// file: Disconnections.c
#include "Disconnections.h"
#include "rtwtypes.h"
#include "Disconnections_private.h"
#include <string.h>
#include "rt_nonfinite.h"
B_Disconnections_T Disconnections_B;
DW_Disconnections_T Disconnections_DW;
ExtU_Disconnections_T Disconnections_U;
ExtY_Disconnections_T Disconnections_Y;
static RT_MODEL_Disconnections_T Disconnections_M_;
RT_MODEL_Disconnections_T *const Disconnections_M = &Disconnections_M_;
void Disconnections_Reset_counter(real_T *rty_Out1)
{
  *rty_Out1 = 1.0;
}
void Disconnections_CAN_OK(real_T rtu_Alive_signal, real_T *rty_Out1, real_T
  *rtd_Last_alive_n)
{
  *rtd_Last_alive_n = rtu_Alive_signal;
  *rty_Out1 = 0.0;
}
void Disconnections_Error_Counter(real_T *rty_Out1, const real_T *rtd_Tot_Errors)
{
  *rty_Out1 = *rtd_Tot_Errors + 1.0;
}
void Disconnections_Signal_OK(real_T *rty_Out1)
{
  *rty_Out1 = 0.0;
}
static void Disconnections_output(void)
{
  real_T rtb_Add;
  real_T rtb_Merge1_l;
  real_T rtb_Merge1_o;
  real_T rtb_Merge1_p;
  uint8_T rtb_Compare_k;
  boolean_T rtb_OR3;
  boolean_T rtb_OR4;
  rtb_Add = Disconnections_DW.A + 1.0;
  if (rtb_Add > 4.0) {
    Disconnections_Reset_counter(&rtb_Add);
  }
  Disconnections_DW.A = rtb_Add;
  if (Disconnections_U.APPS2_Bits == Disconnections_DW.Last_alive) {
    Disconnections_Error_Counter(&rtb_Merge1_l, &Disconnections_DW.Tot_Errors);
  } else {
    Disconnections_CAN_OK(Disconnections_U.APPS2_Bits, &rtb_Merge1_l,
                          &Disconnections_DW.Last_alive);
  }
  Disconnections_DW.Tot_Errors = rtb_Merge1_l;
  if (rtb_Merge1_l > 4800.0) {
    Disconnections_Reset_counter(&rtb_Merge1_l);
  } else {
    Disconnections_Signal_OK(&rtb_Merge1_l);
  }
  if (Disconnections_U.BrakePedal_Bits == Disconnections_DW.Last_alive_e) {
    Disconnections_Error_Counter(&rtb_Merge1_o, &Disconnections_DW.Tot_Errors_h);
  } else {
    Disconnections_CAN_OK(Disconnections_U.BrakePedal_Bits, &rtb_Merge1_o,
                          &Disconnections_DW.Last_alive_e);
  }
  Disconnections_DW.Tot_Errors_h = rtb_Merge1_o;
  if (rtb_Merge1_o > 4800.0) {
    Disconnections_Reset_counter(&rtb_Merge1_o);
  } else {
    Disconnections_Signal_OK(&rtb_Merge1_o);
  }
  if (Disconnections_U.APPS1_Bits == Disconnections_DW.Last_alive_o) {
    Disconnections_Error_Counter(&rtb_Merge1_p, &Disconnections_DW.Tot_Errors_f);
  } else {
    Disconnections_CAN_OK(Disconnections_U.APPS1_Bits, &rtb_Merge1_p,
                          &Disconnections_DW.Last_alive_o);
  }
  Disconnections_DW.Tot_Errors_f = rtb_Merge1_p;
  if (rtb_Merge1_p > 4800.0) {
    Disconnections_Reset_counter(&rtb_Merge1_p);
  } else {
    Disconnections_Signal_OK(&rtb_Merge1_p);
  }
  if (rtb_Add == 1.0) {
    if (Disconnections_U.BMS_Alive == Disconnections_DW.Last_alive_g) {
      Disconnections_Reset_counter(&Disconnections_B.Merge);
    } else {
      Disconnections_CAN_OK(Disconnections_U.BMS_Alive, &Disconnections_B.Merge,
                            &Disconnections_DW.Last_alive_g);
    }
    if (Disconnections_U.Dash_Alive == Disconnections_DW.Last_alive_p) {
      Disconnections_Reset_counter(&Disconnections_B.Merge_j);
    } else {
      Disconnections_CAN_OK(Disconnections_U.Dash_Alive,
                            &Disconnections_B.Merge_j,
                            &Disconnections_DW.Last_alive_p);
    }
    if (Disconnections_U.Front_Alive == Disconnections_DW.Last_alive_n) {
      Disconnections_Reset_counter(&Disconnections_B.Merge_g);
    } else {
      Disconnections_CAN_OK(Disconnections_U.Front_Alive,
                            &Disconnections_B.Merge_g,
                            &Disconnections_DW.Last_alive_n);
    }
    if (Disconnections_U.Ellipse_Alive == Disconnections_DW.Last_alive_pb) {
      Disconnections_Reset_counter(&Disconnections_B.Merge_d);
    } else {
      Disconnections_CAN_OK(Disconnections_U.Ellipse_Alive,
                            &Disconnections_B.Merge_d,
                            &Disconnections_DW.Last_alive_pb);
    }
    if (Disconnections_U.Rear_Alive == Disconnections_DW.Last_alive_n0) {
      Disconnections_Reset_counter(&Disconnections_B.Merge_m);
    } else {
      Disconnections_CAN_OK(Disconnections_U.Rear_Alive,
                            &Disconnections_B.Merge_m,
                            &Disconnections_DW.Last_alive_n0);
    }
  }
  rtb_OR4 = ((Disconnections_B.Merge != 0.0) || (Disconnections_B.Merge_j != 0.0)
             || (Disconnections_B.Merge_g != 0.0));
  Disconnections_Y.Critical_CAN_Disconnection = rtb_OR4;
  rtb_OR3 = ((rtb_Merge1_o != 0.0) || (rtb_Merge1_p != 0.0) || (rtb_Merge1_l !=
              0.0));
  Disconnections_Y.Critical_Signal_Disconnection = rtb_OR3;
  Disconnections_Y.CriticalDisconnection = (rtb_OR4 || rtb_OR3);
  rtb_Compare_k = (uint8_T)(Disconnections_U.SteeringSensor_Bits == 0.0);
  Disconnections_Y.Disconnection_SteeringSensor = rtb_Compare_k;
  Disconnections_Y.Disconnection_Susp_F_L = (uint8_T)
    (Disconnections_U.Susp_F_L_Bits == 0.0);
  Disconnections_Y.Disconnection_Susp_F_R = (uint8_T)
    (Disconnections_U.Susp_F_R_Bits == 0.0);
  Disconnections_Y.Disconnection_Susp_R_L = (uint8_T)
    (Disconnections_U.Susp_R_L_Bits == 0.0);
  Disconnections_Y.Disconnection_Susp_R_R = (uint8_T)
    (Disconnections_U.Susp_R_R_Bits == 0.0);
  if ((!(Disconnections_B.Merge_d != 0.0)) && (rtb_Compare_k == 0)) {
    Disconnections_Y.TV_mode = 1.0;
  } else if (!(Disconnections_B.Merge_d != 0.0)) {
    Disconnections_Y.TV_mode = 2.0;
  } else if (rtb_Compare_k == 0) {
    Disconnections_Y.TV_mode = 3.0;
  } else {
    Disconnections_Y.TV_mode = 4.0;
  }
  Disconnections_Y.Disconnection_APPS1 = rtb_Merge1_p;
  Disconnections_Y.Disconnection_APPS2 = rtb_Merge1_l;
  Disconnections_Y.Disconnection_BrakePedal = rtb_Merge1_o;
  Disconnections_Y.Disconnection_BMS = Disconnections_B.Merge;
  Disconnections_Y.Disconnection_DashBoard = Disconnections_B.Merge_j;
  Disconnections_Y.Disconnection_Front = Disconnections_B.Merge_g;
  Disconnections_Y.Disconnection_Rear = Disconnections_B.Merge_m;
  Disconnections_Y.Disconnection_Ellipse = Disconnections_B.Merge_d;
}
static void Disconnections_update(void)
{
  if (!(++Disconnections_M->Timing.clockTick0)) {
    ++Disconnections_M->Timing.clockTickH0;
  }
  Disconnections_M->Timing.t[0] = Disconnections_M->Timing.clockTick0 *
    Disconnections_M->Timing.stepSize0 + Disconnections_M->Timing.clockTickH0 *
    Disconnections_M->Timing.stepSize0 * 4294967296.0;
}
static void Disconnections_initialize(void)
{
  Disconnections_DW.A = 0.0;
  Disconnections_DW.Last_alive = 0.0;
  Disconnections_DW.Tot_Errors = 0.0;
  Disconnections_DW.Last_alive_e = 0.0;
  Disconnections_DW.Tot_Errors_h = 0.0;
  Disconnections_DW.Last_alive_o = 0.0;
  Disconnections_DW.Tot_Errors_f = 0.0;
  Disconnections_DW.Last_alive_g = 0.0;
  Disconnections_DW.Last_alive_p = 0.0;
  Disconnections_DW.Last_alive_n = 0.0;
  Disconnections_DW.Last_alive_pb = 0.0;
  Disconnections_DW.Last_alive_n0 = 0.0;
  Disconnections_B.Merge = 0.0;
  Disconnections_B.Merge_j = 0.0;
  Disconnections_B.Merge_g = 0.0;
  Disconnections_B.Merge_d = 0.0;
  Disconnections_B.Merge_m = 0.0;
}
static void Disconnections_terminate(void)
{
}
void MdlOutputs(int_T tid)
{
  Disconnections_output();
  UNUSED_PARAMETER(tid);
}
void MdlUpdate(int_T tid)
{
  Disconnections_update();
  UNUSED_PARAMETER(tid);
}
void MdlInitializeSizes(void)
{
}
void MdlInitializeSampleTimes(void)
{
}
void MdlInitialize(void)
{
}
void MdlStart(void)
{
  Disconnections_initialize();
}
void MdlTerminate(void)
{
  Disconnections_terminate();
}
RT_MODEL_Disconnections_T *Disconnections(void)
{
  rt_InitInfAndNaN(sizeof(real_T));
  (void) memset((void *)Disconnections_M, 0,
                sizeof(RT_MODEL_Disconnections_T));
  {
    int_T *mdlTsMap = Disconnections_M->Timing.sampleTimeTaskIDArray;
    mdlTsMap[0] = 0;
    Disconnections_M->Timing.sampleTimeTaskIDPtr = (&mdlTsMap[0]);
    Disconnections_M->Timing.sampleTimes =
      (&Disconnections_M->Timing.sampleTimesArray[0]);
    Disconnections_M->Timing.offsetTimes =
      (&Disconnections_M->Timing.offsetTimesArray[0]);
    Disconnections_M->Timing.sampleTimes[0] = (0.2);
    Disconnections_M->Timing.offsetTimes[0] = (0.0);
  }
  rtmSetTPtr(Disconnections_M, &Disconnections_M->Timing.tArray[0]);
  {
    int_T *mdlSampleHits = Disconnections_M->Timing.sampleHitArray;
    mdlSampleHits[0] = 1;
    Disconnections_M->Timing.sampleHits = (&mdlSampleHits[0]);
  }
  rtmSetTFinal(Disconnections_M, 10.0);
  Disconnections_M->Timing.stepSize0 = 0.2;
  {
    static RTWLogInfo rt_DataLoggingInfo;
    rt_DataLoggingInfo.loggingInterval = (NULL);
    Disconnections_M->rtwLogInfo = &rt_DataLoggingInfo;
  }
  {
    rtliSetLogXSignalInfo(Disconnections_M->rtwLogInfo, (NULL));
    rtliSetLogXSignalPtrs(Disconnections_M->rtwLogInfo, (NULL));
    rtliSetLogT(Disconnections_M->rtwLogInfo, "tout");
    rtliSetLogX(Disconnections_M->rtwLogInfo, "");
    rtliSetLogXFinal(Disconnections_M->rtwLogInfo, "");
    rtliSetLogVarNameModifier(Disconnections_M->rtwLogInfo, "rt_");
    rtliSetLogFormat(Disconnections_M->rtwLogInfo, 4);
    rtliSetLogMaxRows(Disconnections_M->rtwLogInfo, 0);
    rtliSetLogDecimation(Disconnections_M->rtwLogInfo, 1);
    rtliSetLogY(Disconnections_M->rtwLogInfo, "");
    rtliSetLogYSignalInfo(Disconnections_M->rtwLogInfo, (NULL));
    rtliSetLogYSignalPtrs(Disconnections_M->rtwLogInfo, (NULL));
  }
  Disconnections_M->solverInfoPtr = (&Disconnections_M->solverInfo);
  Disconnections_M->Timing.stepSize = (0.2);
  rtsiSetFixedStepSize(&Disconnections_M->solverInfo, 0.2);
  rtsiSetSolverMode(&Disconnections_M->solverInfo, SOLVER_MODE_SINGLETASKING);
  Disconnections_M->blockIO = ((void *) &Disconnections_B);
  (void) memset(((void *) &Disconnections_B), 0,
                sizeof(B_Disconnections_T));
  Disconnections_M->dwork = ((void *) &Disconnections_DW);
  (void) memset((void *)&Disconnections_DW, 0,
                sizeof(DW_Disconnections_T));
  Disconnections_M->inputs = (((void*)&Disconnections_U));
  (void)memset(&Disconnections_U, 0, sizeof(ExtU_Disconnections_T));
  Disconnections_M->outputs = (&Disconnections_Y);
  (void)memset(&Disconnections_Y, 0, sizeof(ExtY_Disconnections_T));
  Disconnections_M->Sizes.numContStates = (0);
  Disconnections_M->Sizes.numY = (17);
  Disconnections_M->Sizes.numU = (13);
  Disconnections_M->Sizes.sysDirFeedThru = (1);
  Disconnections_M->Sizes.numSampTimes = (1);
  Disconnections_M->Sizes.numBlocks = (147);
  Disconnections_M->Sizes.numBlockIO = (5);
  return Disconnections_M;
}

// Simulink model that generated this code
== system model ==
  BMS_Alive : Inport
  Dash_Alive : Inport
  Front_Alive : Inport
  Ellipse_Alive : Inport
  Rear_Alive : Inport
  APPS1_Bits : Inport
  APPS2_Bits : Inport
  BrakePedal_Bits : Inport
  SteeringSensor_Bits : Inport
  Susp_F_L_Bits : Inport
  Susp_F_R_Bits : Inport
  Susp_R_L_Bits : Inport
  Susp_R_R_Bits : Inport
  Critical_CAN_Disconnection : Outport  <- 1: OR4
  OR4 : Logic  Operator=OR  Inputs=3  <- 1: Subsystem#1, 2: Subsystem#1/2, 3: Subsystem#1/3
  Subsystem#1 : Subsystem  <- 1: BMS_Alive, 2: Dash_Alive, 3: Front_Alive, 4: Ellipse_Alive, 5: Rear_Alive, Action: If#1
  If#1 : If  IfExpression=u1 == 1  <- 1: Merge#1
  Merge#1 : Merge  <- 1: Reset_counter, 2: Subsystem#2
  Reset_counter : Subsystem  <- Action: If#2
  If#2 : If  IfExpression=u1 > u2  <- 1: Add, 2: Constant#1
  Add : Sum  <- 1: DataStoreRead#1, 2: Constant#2
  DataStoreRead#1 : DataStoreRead  Indices=1
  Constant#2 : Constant
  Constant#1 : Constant  Value=4
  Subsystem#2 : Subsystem  <- 1: Add, Action: If#2/2
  Critical_Signal_Disconnection : Outport  <- 1: OR3
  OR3 : Logic  Operator=OR  Inputs=3  <- 1: Merge1, 2: Merge#2, 3: Merge#3
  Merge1 : Merge  <- 1: Subsystem#3, 2: Signal_OK
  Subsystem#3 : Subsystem  <- Action: If#3
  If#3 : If  IfExpression=u1>u2  <- 1: Merge, 2: Constant#3
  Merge : Merge  <- 1: Error_Counter, 2: CAN_OK
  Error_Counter : Subsystem  <- Action: If#4
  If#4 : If  IfExpression=u1==u2  <- 1: BrakePedal_Bits, 2: DataStoreRead#2
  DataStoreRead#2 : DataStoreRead  DataStoreName=Last_alive  Indices=1
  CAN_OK : Subsystem  <- 1: BrakePedal_Bits, Action: If#4/2
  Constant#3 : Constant  Value=4800
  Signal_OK : Subsystem  <- Action: If#3/2
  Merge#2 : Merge  <- 1: Subsystem#4, 2: Subsystem#5
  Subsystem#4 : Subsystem  <- Action: If#5
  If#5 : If  IfExpression=u1>u2  <- 1: Merge#4, 2: Constant#3
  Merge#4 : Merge  <- 1: Subsystem#6, 2: Subsystem#7
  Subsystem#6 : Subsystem  <- Action: If#6
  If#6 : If  IfExpression=u1==u2  <- 1: APPS1_Bits, 2: DataStoreRead#3
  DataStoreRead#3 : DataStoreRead  DataStoreName=Last_alive  Indices=1
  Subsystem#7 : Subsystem  <- 1: APPS1_Bits, Action: If#6/2
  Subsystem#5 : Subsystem  <- Action: If#5/2
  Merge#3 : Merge  <- 1: Subsystem#8, 2: Subsystem#9
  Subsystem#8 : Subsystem  <- Action: If#7
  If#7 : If  IfExpression=u1>u2  <- 1: Merge#5, 2: Constant#3
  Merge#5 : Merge  <- 1: Subsystem#10, 2: Subsystem#11
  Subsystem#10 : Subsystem  <- Action: If#8
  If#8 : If  IfExpression=u1==u2  <- 1: APPS2_Bits, 2: DataStoreRead#4
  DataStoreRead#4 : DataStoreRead  DataStoreName=Last_alive  Indices=1
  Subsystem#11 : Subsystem  <- 1: APPS2_Bits, Action: If#8/2
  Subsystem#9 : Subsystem  <- Action: If#7/2
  CriticalDisconnection : Outport  <- 1: Logic#1
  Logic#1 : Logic  Operator=OR  <- 1: OR4, 2: OR3
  Disconnection_SteeringSensor : Outport  <- 1: CompareToZero#1
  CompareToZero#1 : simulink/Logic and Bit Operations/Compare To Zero  relop===  <- 1: SteeringSensor_Bits
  Disconnection_Susp_F_L : Outport  <- 1: CompareToZero#2
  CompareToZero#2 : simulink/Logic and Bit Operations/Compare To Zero  relop===  <- 1: Susp_F_L_Bits
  Disconnection_Susp_F_R : Outport  <- 1: CompareToZero#3
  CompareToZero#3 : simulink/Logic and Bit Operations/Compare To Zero  relop===  <- 1: Susp_F_R_Bits
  Disconnection_Susp_R_L : Outport  <- 1: CompareToZero#4
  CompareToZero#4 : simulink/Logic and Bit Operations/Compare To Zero  relop===  <- 1: Susp_R_L_Bits
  Disconnection_Susp_R_R : Outport  <- 1: CompareToZero#5
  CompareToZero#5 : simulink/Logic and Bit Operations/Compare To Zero  relop===  <- 1: Susp_R_R_Bits
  TV_mode : Outport  <- 1: Merge#6
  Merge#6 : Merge  <- 1: Subsystem#12, 2: Subsystem#13
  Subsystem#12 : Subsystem  <- Action: If#9
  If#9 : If  IfExpression=u1 ==1  <- 1: Logic#2
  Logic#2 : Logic  Operator=NOT  <- 1: Logic#3
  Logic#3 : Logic  Operator=OR  <- 1: Subsystem#1/4, 2: CompareToZero#1
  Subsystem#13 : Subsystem  <- 1: Merge#7, Action: If#9/2
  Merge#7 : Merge  <- 1: Subsystem#14, 2: Subsystem#15
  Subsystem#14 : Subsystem  <- Action: If#10
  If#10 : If  IfExpression=u1 ==1  <- 1: Logic#4
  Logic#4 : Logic  Operator=NOT  <- 1: Subsystem#1/4
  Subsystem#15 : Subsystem  <- 1: Merge#8, Action: If#10/2
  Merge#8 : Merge  <- 1: Subsystem#16, 2: Subsystem#17
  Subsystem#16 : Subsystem  <- Action: If#11
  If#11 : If  IfExpression=u1 ==1  <- 1: Logic#5
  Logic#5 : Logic  Operator=NOT  <- 1: CompareToZero#1
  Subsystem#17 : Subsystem  <- Action: If#11/2
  Disconnection_APPS1 : Outport  <- 1: Merge#2
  Disconnection_APPS2 : Outport  <- 1: Merge#3
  Disconnection_BrakePedal : Outport  <- 1: Merge1
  Disconnection_BMS : Outport  <- 1: Subsystem#1
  Disconnection_DashBoard : Outport  <- 1: Subsystem#1/2
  Disconnection_Front : Outport  <- 1: Subsystem#1/3
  Disconnection_Rear : Outport  <- 1: Subsystem#1/5
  Disconnection_Ellipse : Outport  <- 1: Subsystem#1/4
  DataStoreWrite#1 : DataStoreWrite  Indices=1  <- 1: Merge#1
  DataStoreWrite#2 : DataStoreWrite  DataStoreName=Tot_Errors  Indices=1  <- 1: Merge#5
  DataStoreWrite#3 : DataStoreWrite  DataStoreName=Tot_Errors  Indices=1  <- 1: Merge
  DataStoreWrite#4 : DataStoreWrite  DataStoreName=Tot_Errors  Indices=1  <- 1: Merge#4
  DataStoreMemory#1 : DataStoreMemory
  DataStoreMemory#2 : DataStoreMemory  DataStoreName=Last_alive
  DataStoreMemory#3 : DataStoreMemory  DataStoreName=Last_alive
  DataStoreMemory#4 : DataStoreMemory  DataStoreName=Last_alive
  DataStoreMemory#5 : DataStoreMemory  DataStoreName=Tot_Errors
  DataStoreMemory#6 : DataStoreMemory  DataStoreName=Tot_Errors
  DataStoreMemory#7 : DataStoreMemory  DataStoreName=Tot_Errors
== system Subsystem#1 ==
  Inport#1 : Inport
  Inport#2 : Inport
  Inport#3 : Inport
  Inport#4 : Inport
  Inport#5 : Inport
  ActionPort#1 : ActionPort
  Outport#1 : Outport  <- 1: Merge#9
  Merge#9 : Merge  <- 1: Subsystem#18, 2: Subsystem#19
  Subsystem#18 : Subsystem  <- Action: If#12
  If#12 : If  IfExpression=u1==u2  <- 1: Inport#1, 2: DataStoreRead#5
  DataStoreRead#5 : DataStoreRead  DataStoreName=Last_alive  Indices=1
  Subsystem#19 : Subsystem  <- 1: Inport#1, Action: If#12/2
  Outport#2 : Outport  <- 1: Merge#10
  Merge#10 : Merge  <- 1: Subsystem#20, 2: Subsystem#21
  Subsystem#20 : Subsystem  <- Action: If#13
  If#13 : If  IfExpression=u1==u2  <- 1: Inport#2, 2: DataStoreRead#6
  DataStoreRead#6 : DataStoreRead  DataStoreName=Last_alive  Indices=1
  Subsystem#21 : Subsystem  <- 1: Inport#2, Action: If#13/2
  Outport#3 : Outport  <- 1: Merge#11
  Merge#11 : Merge  <- 1: Subsystem#22, 2: Subsystem#23
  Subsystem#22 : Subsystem  <- Action: If#14
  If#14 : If  IfExpression=u1==u2  <- 1: Inport#3, 2: DataStoreRead#7
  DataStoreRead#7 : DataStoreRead  DataStoreName=Last_alive  Indices=1
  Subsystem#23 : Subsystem  <- 1: Inport#3, Action: If#14/2
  Outport#4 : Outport  <- 1: Merge#12
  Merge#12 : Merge  <- 1: Subsystem#24, 2: Subsystem#25
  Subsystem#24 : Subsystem  <- Action: If#15
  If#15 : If  IfExpression=u1==u2  <- 1: Inport#4, 2: DataStoreRead#8
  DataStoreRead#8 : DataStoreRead  DataStoreName=Last_alive  Indices=1
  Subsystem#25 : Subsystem  <- 1: Inport#4, Action: If#15/2
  Outport#5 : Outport  <- 1: Merge#13
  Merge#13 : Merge  <- 1: Subsystem#26, 2: Subsystem#27
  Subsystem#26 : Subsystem  <- Action: If#16
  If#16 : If  IfExpression=u1==u2  <- 1: Inport#5, 2: DataStoreRead#9
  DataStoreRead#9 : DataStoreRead  DataStoreName=Last_alive  Indices=1
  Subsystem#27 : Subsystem  <- 1: Inport#5, Action: If#16/2
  DataStoreMemory#8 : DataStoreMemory  DataStoreName=Last_alive
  DataStoreMemory#9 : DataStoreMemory  DataStoreName=Last_alive
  DataStoreMemory#10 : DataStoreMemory  DataStoreName=Last_alive
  DataStoreMemory#11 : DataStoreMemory  DataStoreName=Last_alive
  DataStoreMemory#12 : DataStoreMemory  DataStoreName=Last_alive
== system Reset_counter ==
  ActionPort#2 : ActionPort
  Out1 : Outport  <- 1: Constant#4
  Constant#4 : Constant
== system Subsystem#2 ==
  Inport#6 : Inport
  ActionPort#3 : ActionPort
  Outport#6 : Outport  <- 1: Inport#6
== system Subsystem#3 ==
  ActionPort#4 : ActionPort
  Outport#7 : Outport  <- 1: Constant#5
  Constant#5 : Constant
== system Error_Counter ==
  ActionPort#5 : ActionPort
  Outport#8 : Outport  <- 1: Sum#1
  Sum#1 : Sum  <- 1: DataStoreRead#10, 2: Constant#6
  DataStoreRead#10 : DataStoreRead  DataStoreName=Tot_Errors  Indices=1
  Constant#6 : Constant
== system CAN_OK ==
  Alive_signal : Inport
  ActionPort#6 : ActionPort
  Outport#9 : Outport  <- 1: Constant#7
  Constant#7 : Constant  Value=0
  DataStoreWrite#5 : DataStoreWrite  DataStoreName=Last_alive  Indices=1  <- 1: Alive_signal
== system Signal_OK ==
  ActionPort#7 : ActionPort
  Outport#10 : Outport  <- 1: Constant#8
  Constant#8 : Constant  Value=0
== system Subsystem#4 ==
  ActionPort#8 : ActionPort
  Outport#11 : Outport  <- 1: Constant#9
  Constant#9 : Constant
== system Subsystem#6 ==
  ActionPort#9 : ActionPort
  Outport#12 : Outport  <- 1: Sum#2
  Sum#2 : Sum  <- 1: DataStoreRead#11, 2: Constant#10
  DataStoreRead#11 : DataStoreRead  DataStoreName=Tot_Errors  Indices=1
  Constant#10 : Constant
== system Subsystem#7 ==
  Inport#7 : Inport
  ActionPort#10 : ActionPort
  Outport#13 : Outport  <- 1: Constant#11
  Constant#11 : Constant  Value=0
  DataStoreWrite#6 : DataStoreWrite  DataStoreName=Last_alive  Indices=1  <- 1: Inport#7
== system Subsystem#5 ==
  ActionPort#11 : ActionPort
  Outport#14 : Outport  <- 1: Constant#12
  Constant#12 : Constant  Value=0
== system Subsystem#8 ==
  ActionPort#12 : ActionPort
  Outport#15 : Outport  <- 1: Constant#13
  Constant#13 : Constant
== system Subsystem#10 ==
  ActionPort#13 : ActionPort
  Outport#16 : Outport  <- 1: Sum#3
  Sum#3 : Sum  <- 1: DataStoreRead#12, 2: Constant#14
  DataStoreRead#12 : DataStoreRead  DataStoreName=Tot_Errors  Indices=1
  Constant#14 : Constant
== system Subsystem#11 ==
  Inport#8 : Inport
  ActionPort#14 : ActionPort
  Outport#17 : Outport  <- 1: Constant#15
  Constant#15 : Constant  Value=0
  DataStoreWrite#7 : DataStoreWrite  DataStoreName=Last_alive  Indices=1  <- 1: Inport#8
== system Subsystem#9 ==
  ActionPort#15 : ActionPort
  Outport#18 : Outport  <- 1: Constant#16
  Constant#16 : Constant  Value=0
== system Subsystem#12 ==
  ActionPort#16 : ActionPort
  Outport#19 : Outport  <- 1: Constant#17
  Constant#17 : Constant
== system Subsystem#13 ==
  Inport#9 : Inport
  ActionPort#17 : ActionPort
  Outport#20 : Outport  <- 1: Inport#9
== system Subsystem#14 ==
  ActionPort#18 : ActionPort
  Outport#21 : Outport  <- 1: Constant#18
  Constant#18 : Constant  Value=2
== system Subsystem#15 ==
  Inport#10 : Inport
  ActionPort#19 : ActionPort
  Outport#22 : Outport  <- 1: Inport#10
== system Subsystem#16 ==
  ActionPort#20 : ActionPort
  Outport#23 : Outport  <- 1: Constant#19
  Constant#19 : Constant  Value=3
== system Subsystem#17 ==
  ActionPort#21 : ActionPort
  Outport#24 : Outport  <- 1: Constant#20
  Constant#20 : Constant  Value=4
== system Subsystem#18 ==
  ActionPort#22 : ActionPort
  Outport#25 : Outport  <- 1: Constant#21
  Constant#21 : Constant
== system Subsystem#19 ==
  Inport#11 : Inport
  ActionPort#23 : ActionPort
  Outport#26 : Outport  <- 1: Constant#22
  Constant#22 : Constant  Value=0
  DataStoreWrite#8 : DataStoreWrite  DataStoreName=Last_alive  Indices=1  <- 1: Inport#11
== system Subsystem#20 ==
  ActionPort#24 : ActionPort
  Outport#27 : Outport  <- 1: Constant#23
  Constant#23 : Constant
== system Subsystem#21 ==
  Inport#12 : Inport
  ActionPort#25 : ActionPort
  Outport#28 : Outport  <- 1: Constant#24
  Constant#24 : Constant  Value=0
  DataStoreWrite#9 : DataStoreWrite  DataStoreName=Last_alive  Indices=1  <- 1: Inport#12
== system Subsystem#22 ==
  ActionPort#26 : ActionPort
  Outport#29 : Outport  <- 1: Constant#25
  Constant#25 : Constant
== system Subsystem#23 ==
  Inport#13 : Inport
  ActionPort#27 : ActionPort
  Outport#30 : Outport  <- 1: Constant#26
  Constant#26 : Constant  Value=0
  DataStoreWrite#10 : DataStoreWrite  DataStoreName=Last_alive  Indices=1  <- 1: Inport#13
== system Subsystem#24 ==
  ActionPort#28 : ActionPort
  Outport#31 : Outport  <- 1: Constant#27
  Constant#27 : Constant
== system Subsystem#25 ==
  Inport#14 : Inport
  ActionPort#29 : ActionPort
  Outport#32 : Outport  <- 1: Constant#28
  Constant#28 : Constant  Value=0
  DataStoreWrite#11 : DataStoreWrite  DataStoreName=Last_alive  Indices=1  <- 1: Inport#14
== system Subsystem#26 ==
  ActionPort#30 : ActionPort
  Outport#33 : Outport  <- 1: Constant#29
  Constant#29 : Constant
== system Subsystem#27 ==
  Inport#15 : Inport
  ActionPort#31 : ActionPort
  Outport#34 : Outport  <- 1: Constant#30
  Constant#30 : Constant  Value=0
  DataStoreWrite#12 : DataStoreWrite  DataStoreName=Last_alive  Indices=1  <- 1: Inport#15
